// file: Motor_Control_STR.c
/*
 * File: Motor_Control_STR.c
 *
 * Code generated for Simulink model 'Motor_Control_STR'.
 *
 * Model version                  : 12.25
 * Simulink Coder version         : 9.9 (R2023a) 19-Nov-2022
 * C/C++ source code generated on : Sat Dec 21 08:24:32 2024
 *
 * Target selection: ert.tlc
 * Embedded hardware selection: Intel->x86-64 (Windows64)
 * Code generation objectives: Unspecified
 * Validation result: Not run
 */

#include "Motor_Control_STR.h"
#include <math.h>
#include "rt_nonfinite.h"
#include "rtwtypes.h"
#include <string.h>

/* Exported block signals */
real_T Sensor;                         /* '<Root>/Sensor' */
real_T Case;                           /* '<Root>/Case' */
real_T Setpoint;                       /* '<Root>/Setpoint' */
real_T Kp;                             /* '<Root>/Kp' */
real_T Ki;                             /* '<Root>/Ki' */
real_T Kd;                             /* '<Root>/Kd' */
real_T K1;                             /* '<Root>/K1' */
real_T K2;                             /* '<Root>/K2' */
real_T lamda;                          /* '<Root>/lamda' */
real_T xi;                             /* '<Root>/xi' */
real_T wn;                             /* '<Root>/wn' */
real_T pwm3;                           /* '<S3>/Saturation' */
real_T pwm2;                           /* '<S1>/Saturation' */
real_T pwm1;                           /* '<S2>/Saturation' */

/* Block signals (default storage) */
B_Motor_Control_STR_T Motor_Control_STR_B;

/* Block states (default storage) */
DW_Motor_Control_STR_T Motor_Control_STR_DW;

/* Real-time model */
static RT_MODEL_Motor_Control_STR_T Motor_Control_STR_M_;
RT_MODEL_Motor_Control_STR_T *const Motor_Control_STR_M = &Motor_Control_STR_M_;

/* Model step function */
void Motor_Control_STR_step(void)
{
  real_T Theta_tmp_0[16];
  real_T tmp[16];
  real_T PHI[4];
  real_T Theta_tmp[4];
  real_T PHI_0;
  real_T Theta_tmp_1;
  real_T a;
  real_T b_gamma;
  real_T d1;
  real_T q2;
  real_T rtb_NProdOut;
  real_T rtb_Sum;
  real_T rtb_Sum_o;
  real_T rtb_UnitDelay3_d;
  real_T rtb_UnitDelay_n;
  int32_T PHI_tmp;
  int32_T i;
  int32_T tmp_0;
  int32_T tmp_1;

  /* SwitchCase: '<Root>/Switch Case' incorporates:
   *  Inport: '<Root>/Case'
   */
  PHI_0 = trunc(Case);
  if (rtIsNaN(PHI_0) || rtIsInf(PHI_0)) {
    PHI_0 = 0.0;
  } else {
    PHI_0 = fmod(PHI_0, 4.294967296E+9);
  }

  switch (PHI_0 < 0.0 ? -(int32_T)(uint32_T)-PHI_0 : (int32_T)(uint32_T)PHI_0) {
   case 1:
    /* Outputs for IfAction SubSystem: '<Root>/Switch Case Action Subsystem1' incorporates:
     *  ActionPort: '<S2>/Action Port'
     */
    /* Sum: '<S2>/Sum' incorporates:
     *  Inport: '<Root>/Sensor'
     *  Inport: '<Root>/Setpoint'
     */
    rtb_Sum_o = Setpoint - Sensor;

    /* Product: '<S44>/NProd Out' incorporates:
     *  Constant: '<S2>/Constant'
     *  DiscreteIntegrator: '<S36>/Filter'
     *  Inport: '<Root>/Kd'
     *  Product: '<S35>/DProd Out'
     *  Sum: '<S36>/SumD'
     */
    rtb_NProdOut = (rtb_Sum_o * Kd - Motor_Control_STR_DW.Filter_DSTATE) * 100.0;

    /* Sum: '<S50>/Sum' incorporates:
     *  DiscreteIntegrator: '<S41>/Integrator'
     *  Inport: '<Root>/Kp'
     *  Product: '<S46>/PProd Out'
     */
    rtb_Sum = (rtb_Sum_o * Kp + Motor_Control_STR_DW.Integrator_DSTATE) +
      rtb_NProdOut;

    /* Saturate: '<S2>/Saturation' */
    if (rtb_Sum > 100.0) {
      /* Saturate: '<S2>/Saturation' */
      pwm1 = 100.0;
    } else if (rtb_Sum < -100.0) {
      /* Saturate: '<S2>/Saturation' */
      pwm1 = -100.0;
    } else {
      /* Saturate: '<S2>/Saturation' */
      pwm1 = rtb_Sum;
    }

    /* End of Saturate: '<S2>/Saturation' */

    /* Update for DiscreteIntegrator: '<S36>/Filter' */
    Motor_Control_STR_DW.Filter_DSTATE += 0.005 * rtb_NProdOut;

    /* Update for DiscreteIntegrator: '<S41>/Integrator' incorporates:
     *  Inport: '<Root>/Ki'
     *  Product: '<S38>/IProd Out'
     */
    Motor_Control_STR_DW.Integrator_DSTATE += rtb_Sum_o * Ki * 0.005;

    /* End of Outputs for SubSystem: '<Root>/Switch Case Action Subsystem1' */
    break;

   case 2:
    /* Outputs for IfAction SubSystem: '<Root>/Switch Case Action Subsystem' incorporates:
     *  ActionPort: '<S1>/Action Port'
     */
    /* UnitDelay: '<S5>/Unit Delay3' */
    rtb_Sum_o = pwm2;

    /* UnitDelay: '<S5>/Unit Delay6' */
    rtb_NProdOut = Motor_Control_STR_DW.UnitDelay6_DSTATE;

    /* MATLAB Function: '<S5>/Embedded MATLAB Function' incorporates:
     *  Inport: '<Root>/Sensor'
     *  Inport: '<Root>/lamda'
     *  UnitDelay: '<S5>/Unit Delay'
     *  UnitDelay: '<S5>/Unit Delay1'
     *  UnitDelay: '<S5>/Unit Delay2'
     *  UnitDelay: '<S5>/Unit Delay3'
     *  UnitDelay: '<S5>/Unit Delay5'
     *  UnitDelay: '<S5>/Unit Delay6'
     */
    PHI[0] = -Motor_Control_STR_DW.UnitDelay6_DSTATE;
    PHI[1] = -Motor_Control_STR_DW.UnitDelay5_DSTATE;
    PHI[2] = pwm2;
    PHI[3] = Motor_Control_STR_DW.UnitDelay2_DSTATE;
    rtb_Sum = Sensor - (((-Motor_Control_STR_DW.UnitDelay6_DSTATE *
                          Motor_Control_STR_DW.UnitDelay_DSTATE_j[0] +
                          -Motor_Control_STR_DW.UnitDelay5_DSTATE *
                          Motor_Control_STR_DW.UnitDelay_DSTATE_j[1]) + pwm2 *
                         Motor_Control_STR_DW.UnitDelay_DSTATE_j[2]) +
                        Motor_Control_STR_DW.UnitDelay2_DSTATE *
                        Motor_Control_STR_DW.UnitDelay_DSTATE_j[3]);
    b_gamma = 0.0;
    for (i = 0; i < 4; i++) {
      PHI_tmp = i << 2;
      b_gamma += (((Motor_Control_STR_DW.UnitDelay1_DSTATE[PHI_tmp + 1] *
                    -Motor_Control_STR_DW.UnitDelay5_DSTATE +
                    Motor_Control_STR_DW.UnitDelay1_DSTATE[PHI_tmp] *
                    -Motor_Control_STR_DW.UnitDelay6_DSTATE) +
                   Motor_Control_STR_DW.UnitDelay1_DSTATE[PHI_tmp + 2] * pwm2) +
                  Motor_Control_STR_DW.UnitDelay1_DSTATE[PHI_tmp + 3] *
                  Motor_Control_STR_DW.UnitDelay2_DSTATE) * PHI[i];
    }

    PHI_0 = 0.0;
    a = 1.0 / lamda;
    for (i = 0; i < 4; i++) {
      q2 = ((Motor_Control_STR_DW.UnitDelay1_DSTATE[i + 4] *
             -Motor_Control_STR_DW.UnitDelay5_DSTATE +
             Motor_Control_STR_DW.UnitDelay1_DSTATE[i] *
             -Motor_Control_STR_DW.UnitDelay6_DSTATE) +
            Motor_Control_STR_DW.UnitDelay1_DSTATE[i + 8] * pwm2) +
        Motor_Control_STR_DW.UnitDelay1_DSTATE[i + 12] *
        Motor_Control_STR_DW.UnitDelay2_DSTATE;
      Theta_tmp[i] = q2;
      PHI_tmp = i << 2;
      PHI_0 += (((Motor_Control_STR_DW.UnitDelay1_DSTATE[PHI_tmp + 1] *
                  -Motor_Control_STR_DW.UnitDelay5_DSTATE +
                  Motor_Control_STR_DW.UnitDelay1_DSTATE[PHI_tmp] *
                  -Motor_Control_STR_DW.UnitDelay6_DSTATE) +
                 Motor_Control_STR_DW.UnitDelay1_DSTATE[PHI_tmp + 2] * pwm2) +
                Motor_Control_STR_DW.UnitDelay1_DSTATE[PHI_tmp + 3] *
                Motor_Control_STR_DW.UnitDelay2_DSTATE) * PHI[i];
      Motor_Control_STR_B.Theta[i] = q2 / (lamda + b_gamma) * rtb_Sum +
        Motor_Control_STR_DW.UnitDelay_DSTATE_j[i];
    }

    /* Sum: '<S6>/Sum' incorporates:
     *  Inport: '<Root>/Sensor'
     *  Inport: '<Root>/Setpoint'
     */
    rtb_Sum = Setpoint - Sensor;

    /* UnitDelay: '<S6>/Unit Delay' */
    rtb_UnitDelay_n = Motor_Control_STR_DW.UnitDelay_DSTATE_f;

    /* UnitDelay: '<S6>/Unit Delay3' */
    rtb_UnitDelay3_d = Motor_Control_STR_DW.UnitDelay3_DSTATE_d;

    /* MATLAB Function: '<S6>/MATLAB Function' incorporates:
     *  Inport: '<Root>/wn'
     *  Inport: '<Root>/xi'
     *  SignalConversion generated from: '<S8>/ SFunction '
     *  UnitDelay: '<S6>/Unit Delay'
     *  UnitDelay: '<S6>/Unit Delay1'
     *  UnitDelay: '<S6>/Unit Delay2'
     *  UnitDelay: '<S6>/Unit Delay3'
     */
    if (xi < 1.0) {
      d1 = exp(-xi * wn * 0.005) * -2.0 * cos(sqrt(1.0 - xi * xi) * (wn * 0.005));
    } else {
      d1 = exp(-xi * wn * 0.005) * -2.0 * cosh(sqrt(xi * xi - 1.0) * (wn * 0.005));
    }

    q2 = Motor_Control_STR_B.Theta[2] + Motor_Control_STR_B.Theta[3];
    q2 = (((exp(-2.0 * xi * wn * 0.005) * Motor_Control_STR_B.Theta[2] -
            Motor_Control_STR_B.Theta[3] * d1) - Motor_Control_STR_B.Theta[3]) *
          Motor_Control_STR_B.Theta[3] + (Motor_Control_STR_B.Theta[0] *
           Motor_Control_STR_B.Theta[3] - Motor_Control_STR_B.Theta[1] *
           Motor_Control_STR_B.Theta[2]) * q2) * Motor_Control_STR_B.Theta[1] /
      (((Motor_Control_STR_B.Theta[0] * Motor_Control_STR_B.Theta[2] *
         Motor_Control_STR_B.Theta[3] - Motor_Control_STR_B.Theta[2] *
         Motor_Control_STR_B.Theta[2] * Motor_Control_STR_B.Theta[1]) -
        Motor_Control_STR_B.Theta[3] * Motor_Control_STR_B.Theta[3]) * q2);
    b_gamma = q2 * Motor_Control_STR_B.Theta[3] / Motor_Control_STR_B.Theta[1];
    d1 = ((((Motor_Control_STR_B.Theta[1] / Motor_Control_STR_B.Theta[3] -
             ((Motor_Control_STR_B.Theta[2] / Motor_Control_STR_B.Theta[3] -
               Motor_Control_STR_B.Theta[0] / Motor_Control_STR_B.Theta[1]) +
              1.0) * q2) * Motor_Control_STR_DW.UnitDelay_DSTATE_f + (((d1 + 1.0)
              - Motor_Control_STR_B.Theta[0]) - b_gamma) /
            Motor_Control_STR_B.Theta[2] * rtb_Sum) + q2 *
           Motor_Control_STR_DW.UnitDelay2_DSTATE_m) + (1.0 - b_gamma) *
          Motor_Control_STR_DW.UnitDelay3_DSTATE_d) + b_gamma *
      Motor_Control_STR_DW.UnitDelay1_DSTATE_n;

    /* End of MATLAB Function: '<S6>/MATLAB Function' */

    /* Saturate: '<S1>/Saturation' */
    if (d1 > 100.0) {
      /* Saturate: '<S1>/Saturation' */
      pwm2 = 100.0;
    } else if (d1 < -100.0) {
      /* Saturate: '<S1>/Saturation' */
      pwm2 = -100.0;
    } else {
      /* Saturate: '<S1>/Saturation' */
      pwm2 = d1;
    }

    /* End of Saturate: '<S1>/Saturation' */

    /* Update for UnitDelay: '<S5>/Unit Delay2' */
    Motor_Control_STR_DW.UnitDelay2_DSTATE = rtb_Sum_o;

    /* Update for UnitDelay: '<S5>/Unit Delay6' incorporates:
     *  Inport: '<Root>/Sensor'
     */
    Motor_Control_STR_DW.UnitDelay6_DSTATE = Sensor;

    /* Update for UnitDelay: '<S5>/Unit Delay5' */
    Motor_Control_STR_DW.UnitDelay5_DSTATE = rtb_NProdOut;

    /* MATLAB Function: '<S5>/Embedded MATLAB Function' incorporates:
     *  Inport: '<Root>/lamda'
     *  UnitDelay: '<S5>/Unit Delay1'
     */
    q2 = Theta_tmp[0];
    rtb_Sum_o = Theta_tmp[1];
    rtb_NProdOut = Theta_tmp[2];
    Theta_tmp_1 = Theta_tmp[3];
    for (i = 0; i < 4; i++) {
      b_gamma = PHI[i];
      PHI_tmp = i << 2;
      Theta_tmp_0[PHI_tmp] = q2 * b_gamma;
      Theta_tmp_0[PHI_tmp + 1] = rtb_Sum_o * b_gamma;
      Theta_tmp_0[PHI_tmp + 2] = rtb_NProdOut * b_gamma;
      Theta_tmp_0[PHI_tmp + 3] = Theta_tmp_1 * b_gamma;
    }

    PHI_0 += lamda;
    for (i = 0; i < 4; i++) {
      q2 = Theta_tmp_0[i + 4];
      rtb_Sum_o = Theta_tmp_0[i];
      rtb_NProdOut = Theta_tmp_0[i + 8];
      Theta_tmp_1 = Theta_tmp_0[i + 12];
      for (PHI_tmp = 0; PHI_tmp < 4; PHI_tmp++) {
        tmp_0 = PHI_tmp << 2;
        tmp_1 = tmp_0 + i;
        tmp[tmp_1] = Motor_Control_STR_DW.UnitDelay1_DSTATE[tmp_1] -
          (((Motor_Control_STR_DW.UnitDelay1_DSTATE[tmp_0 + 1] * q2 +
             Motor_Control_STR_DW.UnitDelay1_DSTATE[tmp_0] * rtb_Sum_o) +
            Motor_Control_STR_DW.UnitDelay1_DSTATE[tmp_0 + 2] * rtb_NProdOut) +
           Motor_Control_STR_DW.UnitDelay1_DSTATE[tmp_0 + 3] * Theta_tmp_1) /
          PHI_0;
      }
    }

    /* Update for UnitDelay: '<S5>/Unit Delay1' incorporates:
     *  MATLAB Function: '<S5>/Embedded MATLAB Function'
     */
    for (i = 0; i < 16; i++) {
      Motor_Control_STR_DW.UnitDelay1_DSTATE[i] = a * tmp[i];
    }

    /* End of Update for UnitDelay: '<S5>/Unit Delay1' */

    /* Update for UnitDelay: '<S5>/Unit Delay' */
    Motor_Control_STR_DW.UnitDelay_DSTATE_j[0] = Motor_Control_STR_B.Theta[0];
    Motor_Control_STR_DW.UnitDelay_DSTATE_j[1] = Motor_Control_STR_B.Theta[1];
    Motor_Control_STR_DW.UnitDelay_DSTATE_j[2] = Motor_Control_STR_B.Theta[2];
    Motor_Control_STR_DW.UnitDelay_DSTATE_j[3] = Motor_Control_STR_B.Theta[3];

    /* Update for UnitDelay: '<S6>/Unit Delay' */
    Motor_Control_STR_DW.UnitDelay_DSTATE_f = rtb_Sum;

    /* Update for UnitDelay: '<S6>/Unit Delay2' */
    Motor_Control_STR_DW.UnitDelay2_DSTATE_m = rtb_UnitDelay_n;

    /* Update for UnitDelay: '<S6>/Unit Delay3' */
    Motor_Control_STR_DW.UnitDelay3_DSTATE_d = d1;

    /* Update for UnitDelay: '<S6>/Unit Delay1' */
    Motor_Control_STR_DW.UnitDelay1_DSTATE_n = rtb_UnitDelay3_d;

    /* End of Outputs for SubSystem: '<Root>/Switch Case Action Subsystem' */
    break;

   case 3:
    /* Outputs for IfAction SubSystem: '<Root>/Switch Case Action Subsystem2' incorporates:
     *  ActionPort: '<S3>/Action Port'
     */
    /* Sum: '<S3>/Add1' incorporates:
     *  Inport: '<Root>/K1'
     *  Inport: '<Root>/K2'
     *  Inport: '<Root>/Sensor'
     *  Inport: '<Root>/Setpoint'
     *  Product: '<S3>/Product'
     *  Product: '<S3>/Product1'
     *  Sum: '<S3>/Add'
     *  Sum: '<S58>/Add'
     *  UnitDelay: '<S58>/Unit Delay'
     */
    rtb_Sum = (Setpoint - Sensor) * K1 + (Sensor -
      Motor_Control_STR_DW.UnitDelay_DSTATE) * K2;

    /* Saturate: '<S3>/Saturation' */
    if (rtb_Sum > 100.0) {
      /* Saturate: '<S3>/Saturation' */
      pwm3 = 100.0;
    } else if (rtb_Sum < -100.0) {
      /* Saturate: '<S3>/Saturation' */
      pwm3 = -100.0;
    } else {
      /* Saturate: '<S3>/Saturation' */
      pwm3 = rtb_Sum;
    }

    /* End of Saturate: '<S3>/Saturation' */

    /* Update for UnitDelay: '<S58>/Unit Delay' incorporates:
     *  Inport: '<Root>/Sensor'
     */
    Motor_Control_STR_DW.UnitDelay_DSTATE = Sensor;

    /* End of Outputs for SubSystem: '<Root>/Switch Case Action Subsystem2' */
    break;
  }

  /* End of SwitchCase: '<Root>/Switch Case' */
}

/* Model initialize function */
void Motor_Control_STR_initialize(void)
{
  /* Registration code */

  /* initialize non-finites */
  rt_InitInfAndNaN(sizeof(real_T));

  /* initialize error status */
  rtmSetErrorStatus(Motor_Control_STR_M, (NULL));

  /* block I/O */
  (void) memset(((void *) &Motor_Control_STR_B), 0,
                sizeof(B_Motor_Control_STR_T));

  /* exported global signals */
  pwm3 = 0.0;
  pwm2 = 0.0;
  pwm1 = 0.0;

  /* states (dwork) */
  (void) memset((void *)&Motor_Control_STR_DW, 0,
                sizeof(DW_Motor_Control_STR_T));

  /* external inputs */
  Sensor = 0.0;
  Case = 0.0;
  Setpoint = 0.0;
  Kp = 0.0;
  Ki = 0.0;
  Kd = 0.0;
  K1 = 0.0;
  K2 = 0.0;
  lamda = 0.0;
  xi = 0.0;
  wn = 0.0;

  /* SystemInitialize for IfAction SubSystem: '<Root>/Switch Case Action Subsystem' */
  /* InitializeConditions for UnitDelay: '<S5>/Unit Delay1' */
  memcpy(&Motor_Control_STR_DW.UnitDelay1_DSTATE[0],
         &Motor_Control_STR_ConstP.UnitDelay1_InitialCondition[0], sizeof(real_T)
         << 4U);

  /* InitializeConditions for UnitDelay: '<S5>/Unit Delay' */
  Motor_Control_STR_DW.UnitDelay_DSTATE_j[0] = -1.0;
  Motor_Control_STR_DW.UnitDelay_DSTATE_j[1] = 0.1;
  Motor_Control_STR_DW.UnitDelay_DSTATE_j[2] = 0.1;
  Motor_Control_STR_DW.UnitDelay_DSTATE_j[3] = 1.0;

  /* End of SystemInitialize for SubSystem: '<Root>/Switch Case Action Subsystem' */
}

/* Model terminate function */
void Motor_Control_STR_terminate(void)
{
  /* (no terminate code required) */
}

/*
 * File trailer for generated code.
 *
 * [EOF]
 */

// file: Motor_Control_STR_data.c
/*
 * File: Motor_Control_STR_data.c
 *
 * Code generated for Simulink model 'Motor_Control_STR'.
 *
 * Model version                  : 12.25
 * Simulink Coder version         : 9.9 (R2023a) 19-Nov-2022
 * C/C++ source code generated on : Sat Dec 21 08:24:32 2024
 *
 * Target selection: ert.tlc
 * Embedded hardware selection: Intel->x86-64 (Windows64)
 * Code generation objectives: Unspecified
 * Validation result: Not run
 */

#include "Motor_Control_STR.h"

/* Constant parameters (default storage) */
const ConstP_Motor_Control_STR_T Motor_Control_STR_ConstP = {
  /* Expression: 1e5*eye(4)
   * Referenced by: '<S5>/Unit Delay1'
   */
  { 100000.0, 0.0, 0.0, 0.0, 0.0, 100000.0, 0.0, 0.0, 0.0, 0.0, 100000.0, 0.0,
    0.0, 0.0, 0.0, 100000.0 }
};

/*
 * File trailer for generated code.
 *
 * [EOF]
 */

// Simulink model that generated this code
simulink model "Motor_Control_STR"  (R2023a)
settings: Solver=FixedStepDiscrete  StartTime=0.0  StopTime=200  FixedStep=0.005  RelTol=1e-3
libraries: slpidlib x1

== system Motor_Control_STR ==
  Sensor : Inport
  Case : Inport  Port=2
  Setpoint : Inport  Port=3
  Kp : Inport  Port=4
  Ki : Inport  Port=5
  Kd : Inport  Port=6
  K1 : Inport  Port=7
  K2 : Inport  Port=8
  lamda : Inport  Port=9
  xi : Inport  Port=10
  wn : Inport  Port=11
  Switch Case : SwitchCase  CaseConditions={1,2,3}  ShowDefaultCase=off
  Switch Case Action Subsystem : Subsystem  TreatAsAtomicUnit=on
  Switch Case Action Subsystem1 : Subsystem  TreatAsAtomicUnit=on
  Switch Case Action Subsystem2 : Subsystem  TreatAsAtomicUnit=on
  pwm1 : Outport  VectorParamsAs1DForOutWhenUnconnected=off
  pwm2 : Outport  Port=2  VectorParamsAs1DForOutWhenUnconnected=off
  pwm3 : Outport  Port=3  VectorParamsAs1DForOutWhenUnconnected=off
  wires:
  Case/1 -> Switch Case/1  "Case"
  Sensor/1 -> Switch Case Action Subsystem2/2(Sensor), Switch Case Action Subsystem/2(Sensor), Switch Case Action Subsystem1/2(Sensor)  "Sensor"
  Switch Case Action Subsystem1/1(u) -> pwm1/1  "pwm1"
  Switch Case/2 -> Switch Case Action Subsystem/Action
  Switch Case/1 -> Switch Case Action Subsystem1/Action
  Kp/1 -> Switch Case Action Subsystem1/3(Kp)  "Kp"
  Ki/1 -> Switch Case Action Subsystem1/4(Ki)  "Ki"
  Kd/1 -> Switch Case Action Subsystem1/5(Kd)  "Kd"
  Setpoint/1 -> Switch Case Action Subsystem2/1(Setpoint), Switch Case Action Subsystem/1(Setpoint), Switch Case Action Subsystem1/1(Setpoint)  "Setpoint"
  Switch Case Action Subsystem/1(u) -> pwm2/1  "pwm2"
  Switch Case Action Subsystem2/1(u) -> pwm3/1  "pwm3"
  Switch Case/3 -> Switch Case Action Subsystem2/Action
  K2/1 -> Switch Case Action Subsystem2/4(K2)  "K2"
  K1/1 -> Switch Case Action Subsystem2/3(K1)  "K1"
  lamda/1 -> Switch Case Action Subsystem/3(lamda)  "lamda"
  xi/1 -> Switch Case Action Subsystem/4(xi)  "xi"
  wn/1 -> Switch Case Action Subsystem/5(wn)  "wn"

== system Motor_Control_STR/Switch Case Action Subsystem ==
  Setpoint : Inport
  Sensor : Inport  Port=2
  lamda : Inport  Port=3
  xi : Inport  Port=4
  wn : Inport  Port=5
  Action Port : ActionPort  ActionPortLabel=case [ 2 ]:
  DC Motor : Subsystem
  Identification : Subsystem
  Saturation : Saturate  UpperLimit=100  LowerLimit=-100
  Self-Tuning Regulator : Subsystem
  u : Outport  VectorParamsAs1DForOutWhenUnconnected=off
  wires:
  DC Motor/2(Pos (deg)) -> Self-Tuning Regulator/3(yk), Identification/2(yk)
  Sensor/1 -> DC Motor/1(Sensor)
  Saturation/1 -> u/1, Identification/1(uk)
  lamda/1 -> Identification/3(lamda)
  Self-Tuning Regulator/1(u) -> Saturation/1
  Setpoint/1 -> Self-Tuning Regulator/2(wk)
  Identification/1(Theta) -> Self-Tuning Regulator/1(Theta)  "Theta"
  xi/1 -> Self-Tuning Regulator/4(xi)
  wn/1 -> Self-Tuning Regulator/5(wn)

== system Motor_Control_STR/Switch Case Action Subsystem1 ==
  Setpoint : Inport
  Sensor : Inport  Port=2
  Kp : Inport  Port=3
  Ki : Inport  Port=4
  Kd : Inport  Port=5
  Action Port : ActionPort  ActionPortLabel=case [ 1 ]:
  Constant : Constant  Value=100
  Discrete PID Controller : slpidlib/PID Controller  Controller=PID  Form=Parallel  TimeDomain=Discrete-time  UseExternalTs=off  SampleTime=-1  IntegratorMethod=Forward Euler  FilterMethod=Forward Euler  ControllerParametersSource=external  P=1  I=1  UseKiTs=off  D=0  N=100  UseFilter=on  TunerSelectOption=Transfer Function Based (PID Tuner App)  InitialConditionSource=internal  InitialConditionForIntegrator=0  InitialConditionForFilter=0  DifferentiatorICPrevScaledInput=0  ExternalReset=none  TrackingMode=off  Kt=1  LimitOutput=off  SatLimitsSource=internal  UpperSaturationLimit=inf  LowerSaturationLimit=-inf  LinearizeAsGain=off  AntiWindupMode=none  Kb=1  LimitIntegrator=off  UpperIntegratorSaturationLimit=inf  LowerIntegratorSaturationLimit=-inf  POutMin=[]  POutMax=[]  IOutMin=[]  IOutMax=[]  DOutMin=[]  DOutMax=[]  NOutMin=[]  NOutMax=[]  SumOutMin=[]  SumOutMax=[]  SaturationOutMin=[]  SaturationOutMax=[]  PParamMin=[]  PParamMax=[]  IParamMin=[]  IParamMax=[]  DParamMin=[]  DParamMax=[]  NParamMin=[]  NParamMax=[]  KbParamMin=[]  KbParamMax=[]  KtParamMin=[]  KtParamMax=[]  KbOutMin=[]  KbOutMax=[]  KtOutMin=[]  KtOutMax=[]  IntegratorOutMin=[]  IntegratorOutMax=[]  FilterOutMin=[]  FilterOutMax=[]  SumI1OutMin=[]  SumI1OutMax=[]  SumI2OutMin=[]  SumI2OutMax=[]  SumI3OutMin=[]  SumI3OutMax=[]  SumI4OutMin=[]  SumI4OutMax=[]  SumDOutMin=[]  SumDOutMax=[]  DifferentiatorOutMin=[]  DifferentiatorOutMax=[]  FilterDiffOutCoefMin=[]  FilterDiffOutCoefMax=[]  ReciprocalOutMin=[]  ReciprocalOutMax=[]  SumDenOutMin=[]  SumDenOutMax=[]  SumNumOutMin=[]  SumNumOutMax=[]  DivideOutMin=[]  DivideOutMax=[]  UdiffTsProdOutMin=[]  UdiffTsProdOutMax=[]  NTsProdOutMin=[]  NTsProdOutMax=[]  UintegralTsProdOutMin=[]  UintegralTsProdOutMax=[]  UngainTsProdOutMin=[]  UngainTsProdOutMax=[]  ClampingZeroOutDataTypeStr=Inherit: Inherit via back propagation  ClampingZeroOutMin=[]  ClampingZeroOutMax=[]  FilterDenConstantOutDataTypeStr=Inherit: Inherit via back propagation  FilterDenConstantOutMin=[]  FilterDenConstantOutMax=[]  PCopyOutDataTypeStr=Inherit: Inherit via back propagation  PCopyOutMin=[]  PCopyOutMax=[]  NCopyOutDataTypeStr=Inherit: Inherit via back propagation  NCopyOutMin=[]  NCopyOutMax=[]  IntegratorContinuousStateAttributes=''  IntegratorStateMustResolveToSignalObject=off  IntegratorRTWStateStorageClass=Auto  FilterContinuousStateAttributes=''  FilterStateMustResolveToSignalObject=off  FilterRTWStateStorageClass=Auto  ParallelPVariant=ExternalParameters  IdealPVariant=Disabled  IVariant=ExternalParameters  DVariant=ExternalParameters  IntegratorVariant=Discrete  SatVariant=Disabled  AWVariant=Passthrough  PCopyVariant=Disabled  TRVariant=Disabled  FdbkBlocksVariant=Forward  IdealPFdbkVariant=Disabled  SatFdbkVariant=Disabled  DerivativeFilterVariant=ForwardEulerFilter  NVariant=ExternalParameters  NCopyVariant=Disabled  FilterICVariant=InternalICsFilter  IntegratorICVariant=InternalICs  ExternalResetVariant=Disabled  TRSumVariant=Passthrough  SumFdbkVariant=Disabled  SumVariant=Sum_PID  TsampFilterVariant=InternalTs  TsampNgainVariant=Passthrough  TsampIntegralVariant=Disabled_SignalSpec  ExternalSaturationOutDataTypeStr=Inherit: Same as second input
  Saturation : Saturate  UpperLimit=100  LowerLimit=-100
  Sum : Sum  Inputs=|+-
  u : Outport  VectorParamsAs1DForOutWhenUnconnected=off
  wires:
  Setpoint/1 -> Sum/1
  Sensor/1 -> Sum/2
  Sum/1 -> Discrete PID Controller/1
  Kp/1 -> Discrete PID Controller/2
  Ki/1 -> Discrete PID Controller/3
  Kd/1 -> Discrete PID Controller/4
  Constant/1 -> Discrete PID Controller/5
  Discrete PID Controller/1 -> Saturation/1
  Saturation/1 -> u/1

== system Motor_Control_STR/Switch Case Action Subsystem2 ==
  Setpoint : Inport
  Sensor : Inport  Port=2
  K1 : Inport  Port=3
  K2 : Inport  Port=4
  Action Port : ActionPort  ActionPortLabel=case [ 3 ]:
  Add : Sum  Inputs=+-
  Add1 : Sum
  DC Motor : Subsystem
  Product : Product
  Product1 : Product
  Saturation : Saturate  UpperLimit=100  LowerLimit=-100
  u : Outport  VectorParamsAs1DForOutWhenUnconnected=off
  wires:
  Sensor/1 -> DC Motor/1(Sensor)
  Add1/1 -> Saturation/1
  Saturation/1 -> u/1
  Setpoint/1 -> Add/1
  DC Motor/2(Pos (deg)) -> Add/2
  K1/1 -> Product1/1
  Add/1 -> Product1/2
  K2/1 -> Product/2
  DC Motor/1(dPos) -> Product/1
  Product1/1 -> Add1/1
  Product/1 -> Add1/2

== system Motor_Control_STR/Switch Case Action Subsystem/DC Motor ==
  Sensor : Inport
  Add : Sum  Inputs=+-
  Unit Delay : UnitDelay  SampleTime=-1  HasFrameUpgradeWarning=on
  dPos : Outport  VectorParamsAs1DForOutWhenUnconnected=off
  Pos (deg) : Outport  Port=2  VectorParamsAs1DForOutWhenUnconnected=off
  wires:
  Unit Delay/1 -> Add/2
  Sensor/1 -> Unit Delay/1, Pos (deg)/1, Add/1
  Add/1 -> dPos/1

== system Motor_Control_STR/Switch Case Action Subsystem/Identification ==
  uk : Inport  PortDimensions=1
  yk : Inport  Port=2  PortDimensions=1
  lamda : Inport  Port=3  PortDimensions=1
  Embedded MATLAB Function : MATLAB Function  TreatAsAtomicUnit=on
  Mux1 : Mux  Inputs=2
  Mux2 : Mux  Inputs=3
  Unit Delay : UnitDelay  InitialCondition=[-1; 0.1; 0.1; 1]  SampleTime=-1  HasFrameUpgradeWarning=on
  Unit Delay1 : UnitDelay  InitialCondition=1e5*eye(4)  SampleTime=-1  HasFrameUpgradeWarning=on
  Unit Delay{2..3,5..6} (4 alike) : UnitDelay  SampleTime=-1  HasFrameUpgradeWarning=on
  Theta : Outport  PortDimensions=4  VectorParamsAs1DForOutWhenUnconnected=off
  wires:
  Unit Delay/1 -> Embedded MATLAB Function/4(theta_)
  Embedded MATLAB Function/2(theta) -> Unit Delay/1, Theta/1
  Unit Delay1/1 -> Embedded MATLAB Function/3(P_)
  Embedded MATLAB Function/1(P) -> Unit Delay1/1
  Mux1/1 -> Embedded MATLAB Function/1(uk)
  Unit Delay6/1 -> Mux2/2, Unit Delay5/1
  Unit Delay5/1 -> Mux2/3
  Mux2/1 -> Embedded MATLAB Function/2(yk)
  Unit Delay2/1 -> Mux1/2
  Unit Delay3/1 -> Unit Delay2/1, Mux1/1
  uk/1 -> Unit Delay3/1
  yk/1 -> Unit Delay6/1, Mux2/1
  lamda/1 -> Embedded MATLAB Function/5(lamda)

== system Motor_Control_STR/Switch Case Action Subsystem/Self-Tuning Regulator ==
  Theta : Inport
  wk : Inport  Port=2
  yk : Inport  Port=3
  xi : Inport  Port=4
  wn : Inport  Port=5
  MATLAB Function : MATLAB Function  TreatAsAtomicUnit=on
  Mux : Mux  Inputs=3
  Mux1 : Mux  Inputs=2
  Sum : Sum  Inputs=|+-
  Unit Delay{,1..3} (4 alike) : UnitDelay  SampleTime=-1  HasFrameUpgradeWarning=on
  u : Outport  VectorParamsAs1DForOutWhenUnconnected=off
  wires:
  wk/1 -> Sum/1
  Unit Delay/1 -> Mux/2, Unit Delay2/1
  Sum/1 -> Mux/1, Unit Delay/1
  Unit Delay2/1 -> Mux/3
  Theta/1 -> MATLAB Function/1(theta)
  Unit Delay1/1 -> Mux1/2
  Mux1/1 -> MATLAB Function/3(u_)
  Mux/1 -> MATLAB Function/2(e)
  Unit Delay3/1 -> Mux1/1, Unit Delay1/1
  MATLAB Function/1(u) -> Unit Delay3/1, u/1
  yk/1 -> Sum/2  "e"
  xi/1 -> MATLAB Function/4(xi)  "xi"
  wn/1 -> MATLAB Function/5(wn)  "wn"

== system Motor_Control_STR/Switch Case Action Subsystem2/DC Motor ==
  Sensor : Inport
  Add : Sum  Inputs=+-
  Unit Delay : UnitDelay  SampleTime=-1  HasFrameUpgradeWarning=on
  dPos : Outport  VectorParamsAs1DForOutWhenUnconnected=off
  Pos (deg) : Outport  Port=2  VectorParamsAs1DForOutWhenUnconnected=off
  wires:
  Unit Delay/1 -> Add/2
  Sensor/1 -> Unit Delay/1, Pos (deg)/1, Add/1
  Add/1 -> dPos/1

== matlab function Motor_Control_STR/Switch Case Action Subsystem/Self-Tuning Regulator/MATLAB Function ==
function u = STR_pp1(theta,e,u_,xi,wn)
% Cai dat thoi gian lay mau va cuc mong muon
T0 = 0.005;
% xi = 0.99;
% wn = 4;
 
% Gan lai cho de su dung
a1   =  theta(1);
a2   =  theta(2);
b1   =  theta(3);
b2   =  theta(4);
 
% Sinh vien viet bo sung doan code phan dieu khien
 
if( xi<1)
    d1 = -2*exp(-xi*wn*T0)*cos(wn*T0*sqrt(1-xi^2));
else
    d1 = -2*exp(-xi*wn*T0)*cosh(wn*T0*sqrt(xi^2-1));
end
 
d2 = exp(-2*xi*wn*T0);
 
r1 = (b1+b2)*(a1*b1*b2-a2*b1^2-b2^2);
s1 = a2*((b1+b2)*(a1*b2-a2*b1)+b2*(b1*d2-b2*d1-b2));
q2 = s1/r1;
gamma = q2*b2/a2;
q1 = (a2/b2)-q2*(b1/b2-a1/a2+1);
q0 = (d1+1-a1-gamma)/b1;
 
%control law
u = q0*e(1) + q1*e(2) + q2*e(3) + (1-gamma)*u_(1) + gamma*u_(2);

== matlab function Motor_Control_STR/Switch Case Action Subsystem/Identification/Embedded MATLAB Function ==
  settings: fimath=|
      | fimath(...
      | 'RoundMode', 'floor',...
      | 'OverflowMode', 'wrap',...
      | 'ProductMode', 'KeepLSB', 'ProductWordLength', 32,...
      | 'SumMode', 'KeepLSB', 'SumWordLength', 32,...
      | 'CastBeforeSum', false)
function [P,theta] = Uocluong(uk,yk,P_,theta_,lamda)
%lamda = 0.99;
PHI = [-yk(2); -yk(3); uk(1); uk(2)];
e = yk(1) - PHI'*theta_;
L = P_*PHI / (lamda + PHI'*P_*PHI);
P = 1/lamda*(P_ - P_*PHI*PHI'*P_ /(lamda + PHI'*P_*PHI));
theta = theta_ + L*e;
